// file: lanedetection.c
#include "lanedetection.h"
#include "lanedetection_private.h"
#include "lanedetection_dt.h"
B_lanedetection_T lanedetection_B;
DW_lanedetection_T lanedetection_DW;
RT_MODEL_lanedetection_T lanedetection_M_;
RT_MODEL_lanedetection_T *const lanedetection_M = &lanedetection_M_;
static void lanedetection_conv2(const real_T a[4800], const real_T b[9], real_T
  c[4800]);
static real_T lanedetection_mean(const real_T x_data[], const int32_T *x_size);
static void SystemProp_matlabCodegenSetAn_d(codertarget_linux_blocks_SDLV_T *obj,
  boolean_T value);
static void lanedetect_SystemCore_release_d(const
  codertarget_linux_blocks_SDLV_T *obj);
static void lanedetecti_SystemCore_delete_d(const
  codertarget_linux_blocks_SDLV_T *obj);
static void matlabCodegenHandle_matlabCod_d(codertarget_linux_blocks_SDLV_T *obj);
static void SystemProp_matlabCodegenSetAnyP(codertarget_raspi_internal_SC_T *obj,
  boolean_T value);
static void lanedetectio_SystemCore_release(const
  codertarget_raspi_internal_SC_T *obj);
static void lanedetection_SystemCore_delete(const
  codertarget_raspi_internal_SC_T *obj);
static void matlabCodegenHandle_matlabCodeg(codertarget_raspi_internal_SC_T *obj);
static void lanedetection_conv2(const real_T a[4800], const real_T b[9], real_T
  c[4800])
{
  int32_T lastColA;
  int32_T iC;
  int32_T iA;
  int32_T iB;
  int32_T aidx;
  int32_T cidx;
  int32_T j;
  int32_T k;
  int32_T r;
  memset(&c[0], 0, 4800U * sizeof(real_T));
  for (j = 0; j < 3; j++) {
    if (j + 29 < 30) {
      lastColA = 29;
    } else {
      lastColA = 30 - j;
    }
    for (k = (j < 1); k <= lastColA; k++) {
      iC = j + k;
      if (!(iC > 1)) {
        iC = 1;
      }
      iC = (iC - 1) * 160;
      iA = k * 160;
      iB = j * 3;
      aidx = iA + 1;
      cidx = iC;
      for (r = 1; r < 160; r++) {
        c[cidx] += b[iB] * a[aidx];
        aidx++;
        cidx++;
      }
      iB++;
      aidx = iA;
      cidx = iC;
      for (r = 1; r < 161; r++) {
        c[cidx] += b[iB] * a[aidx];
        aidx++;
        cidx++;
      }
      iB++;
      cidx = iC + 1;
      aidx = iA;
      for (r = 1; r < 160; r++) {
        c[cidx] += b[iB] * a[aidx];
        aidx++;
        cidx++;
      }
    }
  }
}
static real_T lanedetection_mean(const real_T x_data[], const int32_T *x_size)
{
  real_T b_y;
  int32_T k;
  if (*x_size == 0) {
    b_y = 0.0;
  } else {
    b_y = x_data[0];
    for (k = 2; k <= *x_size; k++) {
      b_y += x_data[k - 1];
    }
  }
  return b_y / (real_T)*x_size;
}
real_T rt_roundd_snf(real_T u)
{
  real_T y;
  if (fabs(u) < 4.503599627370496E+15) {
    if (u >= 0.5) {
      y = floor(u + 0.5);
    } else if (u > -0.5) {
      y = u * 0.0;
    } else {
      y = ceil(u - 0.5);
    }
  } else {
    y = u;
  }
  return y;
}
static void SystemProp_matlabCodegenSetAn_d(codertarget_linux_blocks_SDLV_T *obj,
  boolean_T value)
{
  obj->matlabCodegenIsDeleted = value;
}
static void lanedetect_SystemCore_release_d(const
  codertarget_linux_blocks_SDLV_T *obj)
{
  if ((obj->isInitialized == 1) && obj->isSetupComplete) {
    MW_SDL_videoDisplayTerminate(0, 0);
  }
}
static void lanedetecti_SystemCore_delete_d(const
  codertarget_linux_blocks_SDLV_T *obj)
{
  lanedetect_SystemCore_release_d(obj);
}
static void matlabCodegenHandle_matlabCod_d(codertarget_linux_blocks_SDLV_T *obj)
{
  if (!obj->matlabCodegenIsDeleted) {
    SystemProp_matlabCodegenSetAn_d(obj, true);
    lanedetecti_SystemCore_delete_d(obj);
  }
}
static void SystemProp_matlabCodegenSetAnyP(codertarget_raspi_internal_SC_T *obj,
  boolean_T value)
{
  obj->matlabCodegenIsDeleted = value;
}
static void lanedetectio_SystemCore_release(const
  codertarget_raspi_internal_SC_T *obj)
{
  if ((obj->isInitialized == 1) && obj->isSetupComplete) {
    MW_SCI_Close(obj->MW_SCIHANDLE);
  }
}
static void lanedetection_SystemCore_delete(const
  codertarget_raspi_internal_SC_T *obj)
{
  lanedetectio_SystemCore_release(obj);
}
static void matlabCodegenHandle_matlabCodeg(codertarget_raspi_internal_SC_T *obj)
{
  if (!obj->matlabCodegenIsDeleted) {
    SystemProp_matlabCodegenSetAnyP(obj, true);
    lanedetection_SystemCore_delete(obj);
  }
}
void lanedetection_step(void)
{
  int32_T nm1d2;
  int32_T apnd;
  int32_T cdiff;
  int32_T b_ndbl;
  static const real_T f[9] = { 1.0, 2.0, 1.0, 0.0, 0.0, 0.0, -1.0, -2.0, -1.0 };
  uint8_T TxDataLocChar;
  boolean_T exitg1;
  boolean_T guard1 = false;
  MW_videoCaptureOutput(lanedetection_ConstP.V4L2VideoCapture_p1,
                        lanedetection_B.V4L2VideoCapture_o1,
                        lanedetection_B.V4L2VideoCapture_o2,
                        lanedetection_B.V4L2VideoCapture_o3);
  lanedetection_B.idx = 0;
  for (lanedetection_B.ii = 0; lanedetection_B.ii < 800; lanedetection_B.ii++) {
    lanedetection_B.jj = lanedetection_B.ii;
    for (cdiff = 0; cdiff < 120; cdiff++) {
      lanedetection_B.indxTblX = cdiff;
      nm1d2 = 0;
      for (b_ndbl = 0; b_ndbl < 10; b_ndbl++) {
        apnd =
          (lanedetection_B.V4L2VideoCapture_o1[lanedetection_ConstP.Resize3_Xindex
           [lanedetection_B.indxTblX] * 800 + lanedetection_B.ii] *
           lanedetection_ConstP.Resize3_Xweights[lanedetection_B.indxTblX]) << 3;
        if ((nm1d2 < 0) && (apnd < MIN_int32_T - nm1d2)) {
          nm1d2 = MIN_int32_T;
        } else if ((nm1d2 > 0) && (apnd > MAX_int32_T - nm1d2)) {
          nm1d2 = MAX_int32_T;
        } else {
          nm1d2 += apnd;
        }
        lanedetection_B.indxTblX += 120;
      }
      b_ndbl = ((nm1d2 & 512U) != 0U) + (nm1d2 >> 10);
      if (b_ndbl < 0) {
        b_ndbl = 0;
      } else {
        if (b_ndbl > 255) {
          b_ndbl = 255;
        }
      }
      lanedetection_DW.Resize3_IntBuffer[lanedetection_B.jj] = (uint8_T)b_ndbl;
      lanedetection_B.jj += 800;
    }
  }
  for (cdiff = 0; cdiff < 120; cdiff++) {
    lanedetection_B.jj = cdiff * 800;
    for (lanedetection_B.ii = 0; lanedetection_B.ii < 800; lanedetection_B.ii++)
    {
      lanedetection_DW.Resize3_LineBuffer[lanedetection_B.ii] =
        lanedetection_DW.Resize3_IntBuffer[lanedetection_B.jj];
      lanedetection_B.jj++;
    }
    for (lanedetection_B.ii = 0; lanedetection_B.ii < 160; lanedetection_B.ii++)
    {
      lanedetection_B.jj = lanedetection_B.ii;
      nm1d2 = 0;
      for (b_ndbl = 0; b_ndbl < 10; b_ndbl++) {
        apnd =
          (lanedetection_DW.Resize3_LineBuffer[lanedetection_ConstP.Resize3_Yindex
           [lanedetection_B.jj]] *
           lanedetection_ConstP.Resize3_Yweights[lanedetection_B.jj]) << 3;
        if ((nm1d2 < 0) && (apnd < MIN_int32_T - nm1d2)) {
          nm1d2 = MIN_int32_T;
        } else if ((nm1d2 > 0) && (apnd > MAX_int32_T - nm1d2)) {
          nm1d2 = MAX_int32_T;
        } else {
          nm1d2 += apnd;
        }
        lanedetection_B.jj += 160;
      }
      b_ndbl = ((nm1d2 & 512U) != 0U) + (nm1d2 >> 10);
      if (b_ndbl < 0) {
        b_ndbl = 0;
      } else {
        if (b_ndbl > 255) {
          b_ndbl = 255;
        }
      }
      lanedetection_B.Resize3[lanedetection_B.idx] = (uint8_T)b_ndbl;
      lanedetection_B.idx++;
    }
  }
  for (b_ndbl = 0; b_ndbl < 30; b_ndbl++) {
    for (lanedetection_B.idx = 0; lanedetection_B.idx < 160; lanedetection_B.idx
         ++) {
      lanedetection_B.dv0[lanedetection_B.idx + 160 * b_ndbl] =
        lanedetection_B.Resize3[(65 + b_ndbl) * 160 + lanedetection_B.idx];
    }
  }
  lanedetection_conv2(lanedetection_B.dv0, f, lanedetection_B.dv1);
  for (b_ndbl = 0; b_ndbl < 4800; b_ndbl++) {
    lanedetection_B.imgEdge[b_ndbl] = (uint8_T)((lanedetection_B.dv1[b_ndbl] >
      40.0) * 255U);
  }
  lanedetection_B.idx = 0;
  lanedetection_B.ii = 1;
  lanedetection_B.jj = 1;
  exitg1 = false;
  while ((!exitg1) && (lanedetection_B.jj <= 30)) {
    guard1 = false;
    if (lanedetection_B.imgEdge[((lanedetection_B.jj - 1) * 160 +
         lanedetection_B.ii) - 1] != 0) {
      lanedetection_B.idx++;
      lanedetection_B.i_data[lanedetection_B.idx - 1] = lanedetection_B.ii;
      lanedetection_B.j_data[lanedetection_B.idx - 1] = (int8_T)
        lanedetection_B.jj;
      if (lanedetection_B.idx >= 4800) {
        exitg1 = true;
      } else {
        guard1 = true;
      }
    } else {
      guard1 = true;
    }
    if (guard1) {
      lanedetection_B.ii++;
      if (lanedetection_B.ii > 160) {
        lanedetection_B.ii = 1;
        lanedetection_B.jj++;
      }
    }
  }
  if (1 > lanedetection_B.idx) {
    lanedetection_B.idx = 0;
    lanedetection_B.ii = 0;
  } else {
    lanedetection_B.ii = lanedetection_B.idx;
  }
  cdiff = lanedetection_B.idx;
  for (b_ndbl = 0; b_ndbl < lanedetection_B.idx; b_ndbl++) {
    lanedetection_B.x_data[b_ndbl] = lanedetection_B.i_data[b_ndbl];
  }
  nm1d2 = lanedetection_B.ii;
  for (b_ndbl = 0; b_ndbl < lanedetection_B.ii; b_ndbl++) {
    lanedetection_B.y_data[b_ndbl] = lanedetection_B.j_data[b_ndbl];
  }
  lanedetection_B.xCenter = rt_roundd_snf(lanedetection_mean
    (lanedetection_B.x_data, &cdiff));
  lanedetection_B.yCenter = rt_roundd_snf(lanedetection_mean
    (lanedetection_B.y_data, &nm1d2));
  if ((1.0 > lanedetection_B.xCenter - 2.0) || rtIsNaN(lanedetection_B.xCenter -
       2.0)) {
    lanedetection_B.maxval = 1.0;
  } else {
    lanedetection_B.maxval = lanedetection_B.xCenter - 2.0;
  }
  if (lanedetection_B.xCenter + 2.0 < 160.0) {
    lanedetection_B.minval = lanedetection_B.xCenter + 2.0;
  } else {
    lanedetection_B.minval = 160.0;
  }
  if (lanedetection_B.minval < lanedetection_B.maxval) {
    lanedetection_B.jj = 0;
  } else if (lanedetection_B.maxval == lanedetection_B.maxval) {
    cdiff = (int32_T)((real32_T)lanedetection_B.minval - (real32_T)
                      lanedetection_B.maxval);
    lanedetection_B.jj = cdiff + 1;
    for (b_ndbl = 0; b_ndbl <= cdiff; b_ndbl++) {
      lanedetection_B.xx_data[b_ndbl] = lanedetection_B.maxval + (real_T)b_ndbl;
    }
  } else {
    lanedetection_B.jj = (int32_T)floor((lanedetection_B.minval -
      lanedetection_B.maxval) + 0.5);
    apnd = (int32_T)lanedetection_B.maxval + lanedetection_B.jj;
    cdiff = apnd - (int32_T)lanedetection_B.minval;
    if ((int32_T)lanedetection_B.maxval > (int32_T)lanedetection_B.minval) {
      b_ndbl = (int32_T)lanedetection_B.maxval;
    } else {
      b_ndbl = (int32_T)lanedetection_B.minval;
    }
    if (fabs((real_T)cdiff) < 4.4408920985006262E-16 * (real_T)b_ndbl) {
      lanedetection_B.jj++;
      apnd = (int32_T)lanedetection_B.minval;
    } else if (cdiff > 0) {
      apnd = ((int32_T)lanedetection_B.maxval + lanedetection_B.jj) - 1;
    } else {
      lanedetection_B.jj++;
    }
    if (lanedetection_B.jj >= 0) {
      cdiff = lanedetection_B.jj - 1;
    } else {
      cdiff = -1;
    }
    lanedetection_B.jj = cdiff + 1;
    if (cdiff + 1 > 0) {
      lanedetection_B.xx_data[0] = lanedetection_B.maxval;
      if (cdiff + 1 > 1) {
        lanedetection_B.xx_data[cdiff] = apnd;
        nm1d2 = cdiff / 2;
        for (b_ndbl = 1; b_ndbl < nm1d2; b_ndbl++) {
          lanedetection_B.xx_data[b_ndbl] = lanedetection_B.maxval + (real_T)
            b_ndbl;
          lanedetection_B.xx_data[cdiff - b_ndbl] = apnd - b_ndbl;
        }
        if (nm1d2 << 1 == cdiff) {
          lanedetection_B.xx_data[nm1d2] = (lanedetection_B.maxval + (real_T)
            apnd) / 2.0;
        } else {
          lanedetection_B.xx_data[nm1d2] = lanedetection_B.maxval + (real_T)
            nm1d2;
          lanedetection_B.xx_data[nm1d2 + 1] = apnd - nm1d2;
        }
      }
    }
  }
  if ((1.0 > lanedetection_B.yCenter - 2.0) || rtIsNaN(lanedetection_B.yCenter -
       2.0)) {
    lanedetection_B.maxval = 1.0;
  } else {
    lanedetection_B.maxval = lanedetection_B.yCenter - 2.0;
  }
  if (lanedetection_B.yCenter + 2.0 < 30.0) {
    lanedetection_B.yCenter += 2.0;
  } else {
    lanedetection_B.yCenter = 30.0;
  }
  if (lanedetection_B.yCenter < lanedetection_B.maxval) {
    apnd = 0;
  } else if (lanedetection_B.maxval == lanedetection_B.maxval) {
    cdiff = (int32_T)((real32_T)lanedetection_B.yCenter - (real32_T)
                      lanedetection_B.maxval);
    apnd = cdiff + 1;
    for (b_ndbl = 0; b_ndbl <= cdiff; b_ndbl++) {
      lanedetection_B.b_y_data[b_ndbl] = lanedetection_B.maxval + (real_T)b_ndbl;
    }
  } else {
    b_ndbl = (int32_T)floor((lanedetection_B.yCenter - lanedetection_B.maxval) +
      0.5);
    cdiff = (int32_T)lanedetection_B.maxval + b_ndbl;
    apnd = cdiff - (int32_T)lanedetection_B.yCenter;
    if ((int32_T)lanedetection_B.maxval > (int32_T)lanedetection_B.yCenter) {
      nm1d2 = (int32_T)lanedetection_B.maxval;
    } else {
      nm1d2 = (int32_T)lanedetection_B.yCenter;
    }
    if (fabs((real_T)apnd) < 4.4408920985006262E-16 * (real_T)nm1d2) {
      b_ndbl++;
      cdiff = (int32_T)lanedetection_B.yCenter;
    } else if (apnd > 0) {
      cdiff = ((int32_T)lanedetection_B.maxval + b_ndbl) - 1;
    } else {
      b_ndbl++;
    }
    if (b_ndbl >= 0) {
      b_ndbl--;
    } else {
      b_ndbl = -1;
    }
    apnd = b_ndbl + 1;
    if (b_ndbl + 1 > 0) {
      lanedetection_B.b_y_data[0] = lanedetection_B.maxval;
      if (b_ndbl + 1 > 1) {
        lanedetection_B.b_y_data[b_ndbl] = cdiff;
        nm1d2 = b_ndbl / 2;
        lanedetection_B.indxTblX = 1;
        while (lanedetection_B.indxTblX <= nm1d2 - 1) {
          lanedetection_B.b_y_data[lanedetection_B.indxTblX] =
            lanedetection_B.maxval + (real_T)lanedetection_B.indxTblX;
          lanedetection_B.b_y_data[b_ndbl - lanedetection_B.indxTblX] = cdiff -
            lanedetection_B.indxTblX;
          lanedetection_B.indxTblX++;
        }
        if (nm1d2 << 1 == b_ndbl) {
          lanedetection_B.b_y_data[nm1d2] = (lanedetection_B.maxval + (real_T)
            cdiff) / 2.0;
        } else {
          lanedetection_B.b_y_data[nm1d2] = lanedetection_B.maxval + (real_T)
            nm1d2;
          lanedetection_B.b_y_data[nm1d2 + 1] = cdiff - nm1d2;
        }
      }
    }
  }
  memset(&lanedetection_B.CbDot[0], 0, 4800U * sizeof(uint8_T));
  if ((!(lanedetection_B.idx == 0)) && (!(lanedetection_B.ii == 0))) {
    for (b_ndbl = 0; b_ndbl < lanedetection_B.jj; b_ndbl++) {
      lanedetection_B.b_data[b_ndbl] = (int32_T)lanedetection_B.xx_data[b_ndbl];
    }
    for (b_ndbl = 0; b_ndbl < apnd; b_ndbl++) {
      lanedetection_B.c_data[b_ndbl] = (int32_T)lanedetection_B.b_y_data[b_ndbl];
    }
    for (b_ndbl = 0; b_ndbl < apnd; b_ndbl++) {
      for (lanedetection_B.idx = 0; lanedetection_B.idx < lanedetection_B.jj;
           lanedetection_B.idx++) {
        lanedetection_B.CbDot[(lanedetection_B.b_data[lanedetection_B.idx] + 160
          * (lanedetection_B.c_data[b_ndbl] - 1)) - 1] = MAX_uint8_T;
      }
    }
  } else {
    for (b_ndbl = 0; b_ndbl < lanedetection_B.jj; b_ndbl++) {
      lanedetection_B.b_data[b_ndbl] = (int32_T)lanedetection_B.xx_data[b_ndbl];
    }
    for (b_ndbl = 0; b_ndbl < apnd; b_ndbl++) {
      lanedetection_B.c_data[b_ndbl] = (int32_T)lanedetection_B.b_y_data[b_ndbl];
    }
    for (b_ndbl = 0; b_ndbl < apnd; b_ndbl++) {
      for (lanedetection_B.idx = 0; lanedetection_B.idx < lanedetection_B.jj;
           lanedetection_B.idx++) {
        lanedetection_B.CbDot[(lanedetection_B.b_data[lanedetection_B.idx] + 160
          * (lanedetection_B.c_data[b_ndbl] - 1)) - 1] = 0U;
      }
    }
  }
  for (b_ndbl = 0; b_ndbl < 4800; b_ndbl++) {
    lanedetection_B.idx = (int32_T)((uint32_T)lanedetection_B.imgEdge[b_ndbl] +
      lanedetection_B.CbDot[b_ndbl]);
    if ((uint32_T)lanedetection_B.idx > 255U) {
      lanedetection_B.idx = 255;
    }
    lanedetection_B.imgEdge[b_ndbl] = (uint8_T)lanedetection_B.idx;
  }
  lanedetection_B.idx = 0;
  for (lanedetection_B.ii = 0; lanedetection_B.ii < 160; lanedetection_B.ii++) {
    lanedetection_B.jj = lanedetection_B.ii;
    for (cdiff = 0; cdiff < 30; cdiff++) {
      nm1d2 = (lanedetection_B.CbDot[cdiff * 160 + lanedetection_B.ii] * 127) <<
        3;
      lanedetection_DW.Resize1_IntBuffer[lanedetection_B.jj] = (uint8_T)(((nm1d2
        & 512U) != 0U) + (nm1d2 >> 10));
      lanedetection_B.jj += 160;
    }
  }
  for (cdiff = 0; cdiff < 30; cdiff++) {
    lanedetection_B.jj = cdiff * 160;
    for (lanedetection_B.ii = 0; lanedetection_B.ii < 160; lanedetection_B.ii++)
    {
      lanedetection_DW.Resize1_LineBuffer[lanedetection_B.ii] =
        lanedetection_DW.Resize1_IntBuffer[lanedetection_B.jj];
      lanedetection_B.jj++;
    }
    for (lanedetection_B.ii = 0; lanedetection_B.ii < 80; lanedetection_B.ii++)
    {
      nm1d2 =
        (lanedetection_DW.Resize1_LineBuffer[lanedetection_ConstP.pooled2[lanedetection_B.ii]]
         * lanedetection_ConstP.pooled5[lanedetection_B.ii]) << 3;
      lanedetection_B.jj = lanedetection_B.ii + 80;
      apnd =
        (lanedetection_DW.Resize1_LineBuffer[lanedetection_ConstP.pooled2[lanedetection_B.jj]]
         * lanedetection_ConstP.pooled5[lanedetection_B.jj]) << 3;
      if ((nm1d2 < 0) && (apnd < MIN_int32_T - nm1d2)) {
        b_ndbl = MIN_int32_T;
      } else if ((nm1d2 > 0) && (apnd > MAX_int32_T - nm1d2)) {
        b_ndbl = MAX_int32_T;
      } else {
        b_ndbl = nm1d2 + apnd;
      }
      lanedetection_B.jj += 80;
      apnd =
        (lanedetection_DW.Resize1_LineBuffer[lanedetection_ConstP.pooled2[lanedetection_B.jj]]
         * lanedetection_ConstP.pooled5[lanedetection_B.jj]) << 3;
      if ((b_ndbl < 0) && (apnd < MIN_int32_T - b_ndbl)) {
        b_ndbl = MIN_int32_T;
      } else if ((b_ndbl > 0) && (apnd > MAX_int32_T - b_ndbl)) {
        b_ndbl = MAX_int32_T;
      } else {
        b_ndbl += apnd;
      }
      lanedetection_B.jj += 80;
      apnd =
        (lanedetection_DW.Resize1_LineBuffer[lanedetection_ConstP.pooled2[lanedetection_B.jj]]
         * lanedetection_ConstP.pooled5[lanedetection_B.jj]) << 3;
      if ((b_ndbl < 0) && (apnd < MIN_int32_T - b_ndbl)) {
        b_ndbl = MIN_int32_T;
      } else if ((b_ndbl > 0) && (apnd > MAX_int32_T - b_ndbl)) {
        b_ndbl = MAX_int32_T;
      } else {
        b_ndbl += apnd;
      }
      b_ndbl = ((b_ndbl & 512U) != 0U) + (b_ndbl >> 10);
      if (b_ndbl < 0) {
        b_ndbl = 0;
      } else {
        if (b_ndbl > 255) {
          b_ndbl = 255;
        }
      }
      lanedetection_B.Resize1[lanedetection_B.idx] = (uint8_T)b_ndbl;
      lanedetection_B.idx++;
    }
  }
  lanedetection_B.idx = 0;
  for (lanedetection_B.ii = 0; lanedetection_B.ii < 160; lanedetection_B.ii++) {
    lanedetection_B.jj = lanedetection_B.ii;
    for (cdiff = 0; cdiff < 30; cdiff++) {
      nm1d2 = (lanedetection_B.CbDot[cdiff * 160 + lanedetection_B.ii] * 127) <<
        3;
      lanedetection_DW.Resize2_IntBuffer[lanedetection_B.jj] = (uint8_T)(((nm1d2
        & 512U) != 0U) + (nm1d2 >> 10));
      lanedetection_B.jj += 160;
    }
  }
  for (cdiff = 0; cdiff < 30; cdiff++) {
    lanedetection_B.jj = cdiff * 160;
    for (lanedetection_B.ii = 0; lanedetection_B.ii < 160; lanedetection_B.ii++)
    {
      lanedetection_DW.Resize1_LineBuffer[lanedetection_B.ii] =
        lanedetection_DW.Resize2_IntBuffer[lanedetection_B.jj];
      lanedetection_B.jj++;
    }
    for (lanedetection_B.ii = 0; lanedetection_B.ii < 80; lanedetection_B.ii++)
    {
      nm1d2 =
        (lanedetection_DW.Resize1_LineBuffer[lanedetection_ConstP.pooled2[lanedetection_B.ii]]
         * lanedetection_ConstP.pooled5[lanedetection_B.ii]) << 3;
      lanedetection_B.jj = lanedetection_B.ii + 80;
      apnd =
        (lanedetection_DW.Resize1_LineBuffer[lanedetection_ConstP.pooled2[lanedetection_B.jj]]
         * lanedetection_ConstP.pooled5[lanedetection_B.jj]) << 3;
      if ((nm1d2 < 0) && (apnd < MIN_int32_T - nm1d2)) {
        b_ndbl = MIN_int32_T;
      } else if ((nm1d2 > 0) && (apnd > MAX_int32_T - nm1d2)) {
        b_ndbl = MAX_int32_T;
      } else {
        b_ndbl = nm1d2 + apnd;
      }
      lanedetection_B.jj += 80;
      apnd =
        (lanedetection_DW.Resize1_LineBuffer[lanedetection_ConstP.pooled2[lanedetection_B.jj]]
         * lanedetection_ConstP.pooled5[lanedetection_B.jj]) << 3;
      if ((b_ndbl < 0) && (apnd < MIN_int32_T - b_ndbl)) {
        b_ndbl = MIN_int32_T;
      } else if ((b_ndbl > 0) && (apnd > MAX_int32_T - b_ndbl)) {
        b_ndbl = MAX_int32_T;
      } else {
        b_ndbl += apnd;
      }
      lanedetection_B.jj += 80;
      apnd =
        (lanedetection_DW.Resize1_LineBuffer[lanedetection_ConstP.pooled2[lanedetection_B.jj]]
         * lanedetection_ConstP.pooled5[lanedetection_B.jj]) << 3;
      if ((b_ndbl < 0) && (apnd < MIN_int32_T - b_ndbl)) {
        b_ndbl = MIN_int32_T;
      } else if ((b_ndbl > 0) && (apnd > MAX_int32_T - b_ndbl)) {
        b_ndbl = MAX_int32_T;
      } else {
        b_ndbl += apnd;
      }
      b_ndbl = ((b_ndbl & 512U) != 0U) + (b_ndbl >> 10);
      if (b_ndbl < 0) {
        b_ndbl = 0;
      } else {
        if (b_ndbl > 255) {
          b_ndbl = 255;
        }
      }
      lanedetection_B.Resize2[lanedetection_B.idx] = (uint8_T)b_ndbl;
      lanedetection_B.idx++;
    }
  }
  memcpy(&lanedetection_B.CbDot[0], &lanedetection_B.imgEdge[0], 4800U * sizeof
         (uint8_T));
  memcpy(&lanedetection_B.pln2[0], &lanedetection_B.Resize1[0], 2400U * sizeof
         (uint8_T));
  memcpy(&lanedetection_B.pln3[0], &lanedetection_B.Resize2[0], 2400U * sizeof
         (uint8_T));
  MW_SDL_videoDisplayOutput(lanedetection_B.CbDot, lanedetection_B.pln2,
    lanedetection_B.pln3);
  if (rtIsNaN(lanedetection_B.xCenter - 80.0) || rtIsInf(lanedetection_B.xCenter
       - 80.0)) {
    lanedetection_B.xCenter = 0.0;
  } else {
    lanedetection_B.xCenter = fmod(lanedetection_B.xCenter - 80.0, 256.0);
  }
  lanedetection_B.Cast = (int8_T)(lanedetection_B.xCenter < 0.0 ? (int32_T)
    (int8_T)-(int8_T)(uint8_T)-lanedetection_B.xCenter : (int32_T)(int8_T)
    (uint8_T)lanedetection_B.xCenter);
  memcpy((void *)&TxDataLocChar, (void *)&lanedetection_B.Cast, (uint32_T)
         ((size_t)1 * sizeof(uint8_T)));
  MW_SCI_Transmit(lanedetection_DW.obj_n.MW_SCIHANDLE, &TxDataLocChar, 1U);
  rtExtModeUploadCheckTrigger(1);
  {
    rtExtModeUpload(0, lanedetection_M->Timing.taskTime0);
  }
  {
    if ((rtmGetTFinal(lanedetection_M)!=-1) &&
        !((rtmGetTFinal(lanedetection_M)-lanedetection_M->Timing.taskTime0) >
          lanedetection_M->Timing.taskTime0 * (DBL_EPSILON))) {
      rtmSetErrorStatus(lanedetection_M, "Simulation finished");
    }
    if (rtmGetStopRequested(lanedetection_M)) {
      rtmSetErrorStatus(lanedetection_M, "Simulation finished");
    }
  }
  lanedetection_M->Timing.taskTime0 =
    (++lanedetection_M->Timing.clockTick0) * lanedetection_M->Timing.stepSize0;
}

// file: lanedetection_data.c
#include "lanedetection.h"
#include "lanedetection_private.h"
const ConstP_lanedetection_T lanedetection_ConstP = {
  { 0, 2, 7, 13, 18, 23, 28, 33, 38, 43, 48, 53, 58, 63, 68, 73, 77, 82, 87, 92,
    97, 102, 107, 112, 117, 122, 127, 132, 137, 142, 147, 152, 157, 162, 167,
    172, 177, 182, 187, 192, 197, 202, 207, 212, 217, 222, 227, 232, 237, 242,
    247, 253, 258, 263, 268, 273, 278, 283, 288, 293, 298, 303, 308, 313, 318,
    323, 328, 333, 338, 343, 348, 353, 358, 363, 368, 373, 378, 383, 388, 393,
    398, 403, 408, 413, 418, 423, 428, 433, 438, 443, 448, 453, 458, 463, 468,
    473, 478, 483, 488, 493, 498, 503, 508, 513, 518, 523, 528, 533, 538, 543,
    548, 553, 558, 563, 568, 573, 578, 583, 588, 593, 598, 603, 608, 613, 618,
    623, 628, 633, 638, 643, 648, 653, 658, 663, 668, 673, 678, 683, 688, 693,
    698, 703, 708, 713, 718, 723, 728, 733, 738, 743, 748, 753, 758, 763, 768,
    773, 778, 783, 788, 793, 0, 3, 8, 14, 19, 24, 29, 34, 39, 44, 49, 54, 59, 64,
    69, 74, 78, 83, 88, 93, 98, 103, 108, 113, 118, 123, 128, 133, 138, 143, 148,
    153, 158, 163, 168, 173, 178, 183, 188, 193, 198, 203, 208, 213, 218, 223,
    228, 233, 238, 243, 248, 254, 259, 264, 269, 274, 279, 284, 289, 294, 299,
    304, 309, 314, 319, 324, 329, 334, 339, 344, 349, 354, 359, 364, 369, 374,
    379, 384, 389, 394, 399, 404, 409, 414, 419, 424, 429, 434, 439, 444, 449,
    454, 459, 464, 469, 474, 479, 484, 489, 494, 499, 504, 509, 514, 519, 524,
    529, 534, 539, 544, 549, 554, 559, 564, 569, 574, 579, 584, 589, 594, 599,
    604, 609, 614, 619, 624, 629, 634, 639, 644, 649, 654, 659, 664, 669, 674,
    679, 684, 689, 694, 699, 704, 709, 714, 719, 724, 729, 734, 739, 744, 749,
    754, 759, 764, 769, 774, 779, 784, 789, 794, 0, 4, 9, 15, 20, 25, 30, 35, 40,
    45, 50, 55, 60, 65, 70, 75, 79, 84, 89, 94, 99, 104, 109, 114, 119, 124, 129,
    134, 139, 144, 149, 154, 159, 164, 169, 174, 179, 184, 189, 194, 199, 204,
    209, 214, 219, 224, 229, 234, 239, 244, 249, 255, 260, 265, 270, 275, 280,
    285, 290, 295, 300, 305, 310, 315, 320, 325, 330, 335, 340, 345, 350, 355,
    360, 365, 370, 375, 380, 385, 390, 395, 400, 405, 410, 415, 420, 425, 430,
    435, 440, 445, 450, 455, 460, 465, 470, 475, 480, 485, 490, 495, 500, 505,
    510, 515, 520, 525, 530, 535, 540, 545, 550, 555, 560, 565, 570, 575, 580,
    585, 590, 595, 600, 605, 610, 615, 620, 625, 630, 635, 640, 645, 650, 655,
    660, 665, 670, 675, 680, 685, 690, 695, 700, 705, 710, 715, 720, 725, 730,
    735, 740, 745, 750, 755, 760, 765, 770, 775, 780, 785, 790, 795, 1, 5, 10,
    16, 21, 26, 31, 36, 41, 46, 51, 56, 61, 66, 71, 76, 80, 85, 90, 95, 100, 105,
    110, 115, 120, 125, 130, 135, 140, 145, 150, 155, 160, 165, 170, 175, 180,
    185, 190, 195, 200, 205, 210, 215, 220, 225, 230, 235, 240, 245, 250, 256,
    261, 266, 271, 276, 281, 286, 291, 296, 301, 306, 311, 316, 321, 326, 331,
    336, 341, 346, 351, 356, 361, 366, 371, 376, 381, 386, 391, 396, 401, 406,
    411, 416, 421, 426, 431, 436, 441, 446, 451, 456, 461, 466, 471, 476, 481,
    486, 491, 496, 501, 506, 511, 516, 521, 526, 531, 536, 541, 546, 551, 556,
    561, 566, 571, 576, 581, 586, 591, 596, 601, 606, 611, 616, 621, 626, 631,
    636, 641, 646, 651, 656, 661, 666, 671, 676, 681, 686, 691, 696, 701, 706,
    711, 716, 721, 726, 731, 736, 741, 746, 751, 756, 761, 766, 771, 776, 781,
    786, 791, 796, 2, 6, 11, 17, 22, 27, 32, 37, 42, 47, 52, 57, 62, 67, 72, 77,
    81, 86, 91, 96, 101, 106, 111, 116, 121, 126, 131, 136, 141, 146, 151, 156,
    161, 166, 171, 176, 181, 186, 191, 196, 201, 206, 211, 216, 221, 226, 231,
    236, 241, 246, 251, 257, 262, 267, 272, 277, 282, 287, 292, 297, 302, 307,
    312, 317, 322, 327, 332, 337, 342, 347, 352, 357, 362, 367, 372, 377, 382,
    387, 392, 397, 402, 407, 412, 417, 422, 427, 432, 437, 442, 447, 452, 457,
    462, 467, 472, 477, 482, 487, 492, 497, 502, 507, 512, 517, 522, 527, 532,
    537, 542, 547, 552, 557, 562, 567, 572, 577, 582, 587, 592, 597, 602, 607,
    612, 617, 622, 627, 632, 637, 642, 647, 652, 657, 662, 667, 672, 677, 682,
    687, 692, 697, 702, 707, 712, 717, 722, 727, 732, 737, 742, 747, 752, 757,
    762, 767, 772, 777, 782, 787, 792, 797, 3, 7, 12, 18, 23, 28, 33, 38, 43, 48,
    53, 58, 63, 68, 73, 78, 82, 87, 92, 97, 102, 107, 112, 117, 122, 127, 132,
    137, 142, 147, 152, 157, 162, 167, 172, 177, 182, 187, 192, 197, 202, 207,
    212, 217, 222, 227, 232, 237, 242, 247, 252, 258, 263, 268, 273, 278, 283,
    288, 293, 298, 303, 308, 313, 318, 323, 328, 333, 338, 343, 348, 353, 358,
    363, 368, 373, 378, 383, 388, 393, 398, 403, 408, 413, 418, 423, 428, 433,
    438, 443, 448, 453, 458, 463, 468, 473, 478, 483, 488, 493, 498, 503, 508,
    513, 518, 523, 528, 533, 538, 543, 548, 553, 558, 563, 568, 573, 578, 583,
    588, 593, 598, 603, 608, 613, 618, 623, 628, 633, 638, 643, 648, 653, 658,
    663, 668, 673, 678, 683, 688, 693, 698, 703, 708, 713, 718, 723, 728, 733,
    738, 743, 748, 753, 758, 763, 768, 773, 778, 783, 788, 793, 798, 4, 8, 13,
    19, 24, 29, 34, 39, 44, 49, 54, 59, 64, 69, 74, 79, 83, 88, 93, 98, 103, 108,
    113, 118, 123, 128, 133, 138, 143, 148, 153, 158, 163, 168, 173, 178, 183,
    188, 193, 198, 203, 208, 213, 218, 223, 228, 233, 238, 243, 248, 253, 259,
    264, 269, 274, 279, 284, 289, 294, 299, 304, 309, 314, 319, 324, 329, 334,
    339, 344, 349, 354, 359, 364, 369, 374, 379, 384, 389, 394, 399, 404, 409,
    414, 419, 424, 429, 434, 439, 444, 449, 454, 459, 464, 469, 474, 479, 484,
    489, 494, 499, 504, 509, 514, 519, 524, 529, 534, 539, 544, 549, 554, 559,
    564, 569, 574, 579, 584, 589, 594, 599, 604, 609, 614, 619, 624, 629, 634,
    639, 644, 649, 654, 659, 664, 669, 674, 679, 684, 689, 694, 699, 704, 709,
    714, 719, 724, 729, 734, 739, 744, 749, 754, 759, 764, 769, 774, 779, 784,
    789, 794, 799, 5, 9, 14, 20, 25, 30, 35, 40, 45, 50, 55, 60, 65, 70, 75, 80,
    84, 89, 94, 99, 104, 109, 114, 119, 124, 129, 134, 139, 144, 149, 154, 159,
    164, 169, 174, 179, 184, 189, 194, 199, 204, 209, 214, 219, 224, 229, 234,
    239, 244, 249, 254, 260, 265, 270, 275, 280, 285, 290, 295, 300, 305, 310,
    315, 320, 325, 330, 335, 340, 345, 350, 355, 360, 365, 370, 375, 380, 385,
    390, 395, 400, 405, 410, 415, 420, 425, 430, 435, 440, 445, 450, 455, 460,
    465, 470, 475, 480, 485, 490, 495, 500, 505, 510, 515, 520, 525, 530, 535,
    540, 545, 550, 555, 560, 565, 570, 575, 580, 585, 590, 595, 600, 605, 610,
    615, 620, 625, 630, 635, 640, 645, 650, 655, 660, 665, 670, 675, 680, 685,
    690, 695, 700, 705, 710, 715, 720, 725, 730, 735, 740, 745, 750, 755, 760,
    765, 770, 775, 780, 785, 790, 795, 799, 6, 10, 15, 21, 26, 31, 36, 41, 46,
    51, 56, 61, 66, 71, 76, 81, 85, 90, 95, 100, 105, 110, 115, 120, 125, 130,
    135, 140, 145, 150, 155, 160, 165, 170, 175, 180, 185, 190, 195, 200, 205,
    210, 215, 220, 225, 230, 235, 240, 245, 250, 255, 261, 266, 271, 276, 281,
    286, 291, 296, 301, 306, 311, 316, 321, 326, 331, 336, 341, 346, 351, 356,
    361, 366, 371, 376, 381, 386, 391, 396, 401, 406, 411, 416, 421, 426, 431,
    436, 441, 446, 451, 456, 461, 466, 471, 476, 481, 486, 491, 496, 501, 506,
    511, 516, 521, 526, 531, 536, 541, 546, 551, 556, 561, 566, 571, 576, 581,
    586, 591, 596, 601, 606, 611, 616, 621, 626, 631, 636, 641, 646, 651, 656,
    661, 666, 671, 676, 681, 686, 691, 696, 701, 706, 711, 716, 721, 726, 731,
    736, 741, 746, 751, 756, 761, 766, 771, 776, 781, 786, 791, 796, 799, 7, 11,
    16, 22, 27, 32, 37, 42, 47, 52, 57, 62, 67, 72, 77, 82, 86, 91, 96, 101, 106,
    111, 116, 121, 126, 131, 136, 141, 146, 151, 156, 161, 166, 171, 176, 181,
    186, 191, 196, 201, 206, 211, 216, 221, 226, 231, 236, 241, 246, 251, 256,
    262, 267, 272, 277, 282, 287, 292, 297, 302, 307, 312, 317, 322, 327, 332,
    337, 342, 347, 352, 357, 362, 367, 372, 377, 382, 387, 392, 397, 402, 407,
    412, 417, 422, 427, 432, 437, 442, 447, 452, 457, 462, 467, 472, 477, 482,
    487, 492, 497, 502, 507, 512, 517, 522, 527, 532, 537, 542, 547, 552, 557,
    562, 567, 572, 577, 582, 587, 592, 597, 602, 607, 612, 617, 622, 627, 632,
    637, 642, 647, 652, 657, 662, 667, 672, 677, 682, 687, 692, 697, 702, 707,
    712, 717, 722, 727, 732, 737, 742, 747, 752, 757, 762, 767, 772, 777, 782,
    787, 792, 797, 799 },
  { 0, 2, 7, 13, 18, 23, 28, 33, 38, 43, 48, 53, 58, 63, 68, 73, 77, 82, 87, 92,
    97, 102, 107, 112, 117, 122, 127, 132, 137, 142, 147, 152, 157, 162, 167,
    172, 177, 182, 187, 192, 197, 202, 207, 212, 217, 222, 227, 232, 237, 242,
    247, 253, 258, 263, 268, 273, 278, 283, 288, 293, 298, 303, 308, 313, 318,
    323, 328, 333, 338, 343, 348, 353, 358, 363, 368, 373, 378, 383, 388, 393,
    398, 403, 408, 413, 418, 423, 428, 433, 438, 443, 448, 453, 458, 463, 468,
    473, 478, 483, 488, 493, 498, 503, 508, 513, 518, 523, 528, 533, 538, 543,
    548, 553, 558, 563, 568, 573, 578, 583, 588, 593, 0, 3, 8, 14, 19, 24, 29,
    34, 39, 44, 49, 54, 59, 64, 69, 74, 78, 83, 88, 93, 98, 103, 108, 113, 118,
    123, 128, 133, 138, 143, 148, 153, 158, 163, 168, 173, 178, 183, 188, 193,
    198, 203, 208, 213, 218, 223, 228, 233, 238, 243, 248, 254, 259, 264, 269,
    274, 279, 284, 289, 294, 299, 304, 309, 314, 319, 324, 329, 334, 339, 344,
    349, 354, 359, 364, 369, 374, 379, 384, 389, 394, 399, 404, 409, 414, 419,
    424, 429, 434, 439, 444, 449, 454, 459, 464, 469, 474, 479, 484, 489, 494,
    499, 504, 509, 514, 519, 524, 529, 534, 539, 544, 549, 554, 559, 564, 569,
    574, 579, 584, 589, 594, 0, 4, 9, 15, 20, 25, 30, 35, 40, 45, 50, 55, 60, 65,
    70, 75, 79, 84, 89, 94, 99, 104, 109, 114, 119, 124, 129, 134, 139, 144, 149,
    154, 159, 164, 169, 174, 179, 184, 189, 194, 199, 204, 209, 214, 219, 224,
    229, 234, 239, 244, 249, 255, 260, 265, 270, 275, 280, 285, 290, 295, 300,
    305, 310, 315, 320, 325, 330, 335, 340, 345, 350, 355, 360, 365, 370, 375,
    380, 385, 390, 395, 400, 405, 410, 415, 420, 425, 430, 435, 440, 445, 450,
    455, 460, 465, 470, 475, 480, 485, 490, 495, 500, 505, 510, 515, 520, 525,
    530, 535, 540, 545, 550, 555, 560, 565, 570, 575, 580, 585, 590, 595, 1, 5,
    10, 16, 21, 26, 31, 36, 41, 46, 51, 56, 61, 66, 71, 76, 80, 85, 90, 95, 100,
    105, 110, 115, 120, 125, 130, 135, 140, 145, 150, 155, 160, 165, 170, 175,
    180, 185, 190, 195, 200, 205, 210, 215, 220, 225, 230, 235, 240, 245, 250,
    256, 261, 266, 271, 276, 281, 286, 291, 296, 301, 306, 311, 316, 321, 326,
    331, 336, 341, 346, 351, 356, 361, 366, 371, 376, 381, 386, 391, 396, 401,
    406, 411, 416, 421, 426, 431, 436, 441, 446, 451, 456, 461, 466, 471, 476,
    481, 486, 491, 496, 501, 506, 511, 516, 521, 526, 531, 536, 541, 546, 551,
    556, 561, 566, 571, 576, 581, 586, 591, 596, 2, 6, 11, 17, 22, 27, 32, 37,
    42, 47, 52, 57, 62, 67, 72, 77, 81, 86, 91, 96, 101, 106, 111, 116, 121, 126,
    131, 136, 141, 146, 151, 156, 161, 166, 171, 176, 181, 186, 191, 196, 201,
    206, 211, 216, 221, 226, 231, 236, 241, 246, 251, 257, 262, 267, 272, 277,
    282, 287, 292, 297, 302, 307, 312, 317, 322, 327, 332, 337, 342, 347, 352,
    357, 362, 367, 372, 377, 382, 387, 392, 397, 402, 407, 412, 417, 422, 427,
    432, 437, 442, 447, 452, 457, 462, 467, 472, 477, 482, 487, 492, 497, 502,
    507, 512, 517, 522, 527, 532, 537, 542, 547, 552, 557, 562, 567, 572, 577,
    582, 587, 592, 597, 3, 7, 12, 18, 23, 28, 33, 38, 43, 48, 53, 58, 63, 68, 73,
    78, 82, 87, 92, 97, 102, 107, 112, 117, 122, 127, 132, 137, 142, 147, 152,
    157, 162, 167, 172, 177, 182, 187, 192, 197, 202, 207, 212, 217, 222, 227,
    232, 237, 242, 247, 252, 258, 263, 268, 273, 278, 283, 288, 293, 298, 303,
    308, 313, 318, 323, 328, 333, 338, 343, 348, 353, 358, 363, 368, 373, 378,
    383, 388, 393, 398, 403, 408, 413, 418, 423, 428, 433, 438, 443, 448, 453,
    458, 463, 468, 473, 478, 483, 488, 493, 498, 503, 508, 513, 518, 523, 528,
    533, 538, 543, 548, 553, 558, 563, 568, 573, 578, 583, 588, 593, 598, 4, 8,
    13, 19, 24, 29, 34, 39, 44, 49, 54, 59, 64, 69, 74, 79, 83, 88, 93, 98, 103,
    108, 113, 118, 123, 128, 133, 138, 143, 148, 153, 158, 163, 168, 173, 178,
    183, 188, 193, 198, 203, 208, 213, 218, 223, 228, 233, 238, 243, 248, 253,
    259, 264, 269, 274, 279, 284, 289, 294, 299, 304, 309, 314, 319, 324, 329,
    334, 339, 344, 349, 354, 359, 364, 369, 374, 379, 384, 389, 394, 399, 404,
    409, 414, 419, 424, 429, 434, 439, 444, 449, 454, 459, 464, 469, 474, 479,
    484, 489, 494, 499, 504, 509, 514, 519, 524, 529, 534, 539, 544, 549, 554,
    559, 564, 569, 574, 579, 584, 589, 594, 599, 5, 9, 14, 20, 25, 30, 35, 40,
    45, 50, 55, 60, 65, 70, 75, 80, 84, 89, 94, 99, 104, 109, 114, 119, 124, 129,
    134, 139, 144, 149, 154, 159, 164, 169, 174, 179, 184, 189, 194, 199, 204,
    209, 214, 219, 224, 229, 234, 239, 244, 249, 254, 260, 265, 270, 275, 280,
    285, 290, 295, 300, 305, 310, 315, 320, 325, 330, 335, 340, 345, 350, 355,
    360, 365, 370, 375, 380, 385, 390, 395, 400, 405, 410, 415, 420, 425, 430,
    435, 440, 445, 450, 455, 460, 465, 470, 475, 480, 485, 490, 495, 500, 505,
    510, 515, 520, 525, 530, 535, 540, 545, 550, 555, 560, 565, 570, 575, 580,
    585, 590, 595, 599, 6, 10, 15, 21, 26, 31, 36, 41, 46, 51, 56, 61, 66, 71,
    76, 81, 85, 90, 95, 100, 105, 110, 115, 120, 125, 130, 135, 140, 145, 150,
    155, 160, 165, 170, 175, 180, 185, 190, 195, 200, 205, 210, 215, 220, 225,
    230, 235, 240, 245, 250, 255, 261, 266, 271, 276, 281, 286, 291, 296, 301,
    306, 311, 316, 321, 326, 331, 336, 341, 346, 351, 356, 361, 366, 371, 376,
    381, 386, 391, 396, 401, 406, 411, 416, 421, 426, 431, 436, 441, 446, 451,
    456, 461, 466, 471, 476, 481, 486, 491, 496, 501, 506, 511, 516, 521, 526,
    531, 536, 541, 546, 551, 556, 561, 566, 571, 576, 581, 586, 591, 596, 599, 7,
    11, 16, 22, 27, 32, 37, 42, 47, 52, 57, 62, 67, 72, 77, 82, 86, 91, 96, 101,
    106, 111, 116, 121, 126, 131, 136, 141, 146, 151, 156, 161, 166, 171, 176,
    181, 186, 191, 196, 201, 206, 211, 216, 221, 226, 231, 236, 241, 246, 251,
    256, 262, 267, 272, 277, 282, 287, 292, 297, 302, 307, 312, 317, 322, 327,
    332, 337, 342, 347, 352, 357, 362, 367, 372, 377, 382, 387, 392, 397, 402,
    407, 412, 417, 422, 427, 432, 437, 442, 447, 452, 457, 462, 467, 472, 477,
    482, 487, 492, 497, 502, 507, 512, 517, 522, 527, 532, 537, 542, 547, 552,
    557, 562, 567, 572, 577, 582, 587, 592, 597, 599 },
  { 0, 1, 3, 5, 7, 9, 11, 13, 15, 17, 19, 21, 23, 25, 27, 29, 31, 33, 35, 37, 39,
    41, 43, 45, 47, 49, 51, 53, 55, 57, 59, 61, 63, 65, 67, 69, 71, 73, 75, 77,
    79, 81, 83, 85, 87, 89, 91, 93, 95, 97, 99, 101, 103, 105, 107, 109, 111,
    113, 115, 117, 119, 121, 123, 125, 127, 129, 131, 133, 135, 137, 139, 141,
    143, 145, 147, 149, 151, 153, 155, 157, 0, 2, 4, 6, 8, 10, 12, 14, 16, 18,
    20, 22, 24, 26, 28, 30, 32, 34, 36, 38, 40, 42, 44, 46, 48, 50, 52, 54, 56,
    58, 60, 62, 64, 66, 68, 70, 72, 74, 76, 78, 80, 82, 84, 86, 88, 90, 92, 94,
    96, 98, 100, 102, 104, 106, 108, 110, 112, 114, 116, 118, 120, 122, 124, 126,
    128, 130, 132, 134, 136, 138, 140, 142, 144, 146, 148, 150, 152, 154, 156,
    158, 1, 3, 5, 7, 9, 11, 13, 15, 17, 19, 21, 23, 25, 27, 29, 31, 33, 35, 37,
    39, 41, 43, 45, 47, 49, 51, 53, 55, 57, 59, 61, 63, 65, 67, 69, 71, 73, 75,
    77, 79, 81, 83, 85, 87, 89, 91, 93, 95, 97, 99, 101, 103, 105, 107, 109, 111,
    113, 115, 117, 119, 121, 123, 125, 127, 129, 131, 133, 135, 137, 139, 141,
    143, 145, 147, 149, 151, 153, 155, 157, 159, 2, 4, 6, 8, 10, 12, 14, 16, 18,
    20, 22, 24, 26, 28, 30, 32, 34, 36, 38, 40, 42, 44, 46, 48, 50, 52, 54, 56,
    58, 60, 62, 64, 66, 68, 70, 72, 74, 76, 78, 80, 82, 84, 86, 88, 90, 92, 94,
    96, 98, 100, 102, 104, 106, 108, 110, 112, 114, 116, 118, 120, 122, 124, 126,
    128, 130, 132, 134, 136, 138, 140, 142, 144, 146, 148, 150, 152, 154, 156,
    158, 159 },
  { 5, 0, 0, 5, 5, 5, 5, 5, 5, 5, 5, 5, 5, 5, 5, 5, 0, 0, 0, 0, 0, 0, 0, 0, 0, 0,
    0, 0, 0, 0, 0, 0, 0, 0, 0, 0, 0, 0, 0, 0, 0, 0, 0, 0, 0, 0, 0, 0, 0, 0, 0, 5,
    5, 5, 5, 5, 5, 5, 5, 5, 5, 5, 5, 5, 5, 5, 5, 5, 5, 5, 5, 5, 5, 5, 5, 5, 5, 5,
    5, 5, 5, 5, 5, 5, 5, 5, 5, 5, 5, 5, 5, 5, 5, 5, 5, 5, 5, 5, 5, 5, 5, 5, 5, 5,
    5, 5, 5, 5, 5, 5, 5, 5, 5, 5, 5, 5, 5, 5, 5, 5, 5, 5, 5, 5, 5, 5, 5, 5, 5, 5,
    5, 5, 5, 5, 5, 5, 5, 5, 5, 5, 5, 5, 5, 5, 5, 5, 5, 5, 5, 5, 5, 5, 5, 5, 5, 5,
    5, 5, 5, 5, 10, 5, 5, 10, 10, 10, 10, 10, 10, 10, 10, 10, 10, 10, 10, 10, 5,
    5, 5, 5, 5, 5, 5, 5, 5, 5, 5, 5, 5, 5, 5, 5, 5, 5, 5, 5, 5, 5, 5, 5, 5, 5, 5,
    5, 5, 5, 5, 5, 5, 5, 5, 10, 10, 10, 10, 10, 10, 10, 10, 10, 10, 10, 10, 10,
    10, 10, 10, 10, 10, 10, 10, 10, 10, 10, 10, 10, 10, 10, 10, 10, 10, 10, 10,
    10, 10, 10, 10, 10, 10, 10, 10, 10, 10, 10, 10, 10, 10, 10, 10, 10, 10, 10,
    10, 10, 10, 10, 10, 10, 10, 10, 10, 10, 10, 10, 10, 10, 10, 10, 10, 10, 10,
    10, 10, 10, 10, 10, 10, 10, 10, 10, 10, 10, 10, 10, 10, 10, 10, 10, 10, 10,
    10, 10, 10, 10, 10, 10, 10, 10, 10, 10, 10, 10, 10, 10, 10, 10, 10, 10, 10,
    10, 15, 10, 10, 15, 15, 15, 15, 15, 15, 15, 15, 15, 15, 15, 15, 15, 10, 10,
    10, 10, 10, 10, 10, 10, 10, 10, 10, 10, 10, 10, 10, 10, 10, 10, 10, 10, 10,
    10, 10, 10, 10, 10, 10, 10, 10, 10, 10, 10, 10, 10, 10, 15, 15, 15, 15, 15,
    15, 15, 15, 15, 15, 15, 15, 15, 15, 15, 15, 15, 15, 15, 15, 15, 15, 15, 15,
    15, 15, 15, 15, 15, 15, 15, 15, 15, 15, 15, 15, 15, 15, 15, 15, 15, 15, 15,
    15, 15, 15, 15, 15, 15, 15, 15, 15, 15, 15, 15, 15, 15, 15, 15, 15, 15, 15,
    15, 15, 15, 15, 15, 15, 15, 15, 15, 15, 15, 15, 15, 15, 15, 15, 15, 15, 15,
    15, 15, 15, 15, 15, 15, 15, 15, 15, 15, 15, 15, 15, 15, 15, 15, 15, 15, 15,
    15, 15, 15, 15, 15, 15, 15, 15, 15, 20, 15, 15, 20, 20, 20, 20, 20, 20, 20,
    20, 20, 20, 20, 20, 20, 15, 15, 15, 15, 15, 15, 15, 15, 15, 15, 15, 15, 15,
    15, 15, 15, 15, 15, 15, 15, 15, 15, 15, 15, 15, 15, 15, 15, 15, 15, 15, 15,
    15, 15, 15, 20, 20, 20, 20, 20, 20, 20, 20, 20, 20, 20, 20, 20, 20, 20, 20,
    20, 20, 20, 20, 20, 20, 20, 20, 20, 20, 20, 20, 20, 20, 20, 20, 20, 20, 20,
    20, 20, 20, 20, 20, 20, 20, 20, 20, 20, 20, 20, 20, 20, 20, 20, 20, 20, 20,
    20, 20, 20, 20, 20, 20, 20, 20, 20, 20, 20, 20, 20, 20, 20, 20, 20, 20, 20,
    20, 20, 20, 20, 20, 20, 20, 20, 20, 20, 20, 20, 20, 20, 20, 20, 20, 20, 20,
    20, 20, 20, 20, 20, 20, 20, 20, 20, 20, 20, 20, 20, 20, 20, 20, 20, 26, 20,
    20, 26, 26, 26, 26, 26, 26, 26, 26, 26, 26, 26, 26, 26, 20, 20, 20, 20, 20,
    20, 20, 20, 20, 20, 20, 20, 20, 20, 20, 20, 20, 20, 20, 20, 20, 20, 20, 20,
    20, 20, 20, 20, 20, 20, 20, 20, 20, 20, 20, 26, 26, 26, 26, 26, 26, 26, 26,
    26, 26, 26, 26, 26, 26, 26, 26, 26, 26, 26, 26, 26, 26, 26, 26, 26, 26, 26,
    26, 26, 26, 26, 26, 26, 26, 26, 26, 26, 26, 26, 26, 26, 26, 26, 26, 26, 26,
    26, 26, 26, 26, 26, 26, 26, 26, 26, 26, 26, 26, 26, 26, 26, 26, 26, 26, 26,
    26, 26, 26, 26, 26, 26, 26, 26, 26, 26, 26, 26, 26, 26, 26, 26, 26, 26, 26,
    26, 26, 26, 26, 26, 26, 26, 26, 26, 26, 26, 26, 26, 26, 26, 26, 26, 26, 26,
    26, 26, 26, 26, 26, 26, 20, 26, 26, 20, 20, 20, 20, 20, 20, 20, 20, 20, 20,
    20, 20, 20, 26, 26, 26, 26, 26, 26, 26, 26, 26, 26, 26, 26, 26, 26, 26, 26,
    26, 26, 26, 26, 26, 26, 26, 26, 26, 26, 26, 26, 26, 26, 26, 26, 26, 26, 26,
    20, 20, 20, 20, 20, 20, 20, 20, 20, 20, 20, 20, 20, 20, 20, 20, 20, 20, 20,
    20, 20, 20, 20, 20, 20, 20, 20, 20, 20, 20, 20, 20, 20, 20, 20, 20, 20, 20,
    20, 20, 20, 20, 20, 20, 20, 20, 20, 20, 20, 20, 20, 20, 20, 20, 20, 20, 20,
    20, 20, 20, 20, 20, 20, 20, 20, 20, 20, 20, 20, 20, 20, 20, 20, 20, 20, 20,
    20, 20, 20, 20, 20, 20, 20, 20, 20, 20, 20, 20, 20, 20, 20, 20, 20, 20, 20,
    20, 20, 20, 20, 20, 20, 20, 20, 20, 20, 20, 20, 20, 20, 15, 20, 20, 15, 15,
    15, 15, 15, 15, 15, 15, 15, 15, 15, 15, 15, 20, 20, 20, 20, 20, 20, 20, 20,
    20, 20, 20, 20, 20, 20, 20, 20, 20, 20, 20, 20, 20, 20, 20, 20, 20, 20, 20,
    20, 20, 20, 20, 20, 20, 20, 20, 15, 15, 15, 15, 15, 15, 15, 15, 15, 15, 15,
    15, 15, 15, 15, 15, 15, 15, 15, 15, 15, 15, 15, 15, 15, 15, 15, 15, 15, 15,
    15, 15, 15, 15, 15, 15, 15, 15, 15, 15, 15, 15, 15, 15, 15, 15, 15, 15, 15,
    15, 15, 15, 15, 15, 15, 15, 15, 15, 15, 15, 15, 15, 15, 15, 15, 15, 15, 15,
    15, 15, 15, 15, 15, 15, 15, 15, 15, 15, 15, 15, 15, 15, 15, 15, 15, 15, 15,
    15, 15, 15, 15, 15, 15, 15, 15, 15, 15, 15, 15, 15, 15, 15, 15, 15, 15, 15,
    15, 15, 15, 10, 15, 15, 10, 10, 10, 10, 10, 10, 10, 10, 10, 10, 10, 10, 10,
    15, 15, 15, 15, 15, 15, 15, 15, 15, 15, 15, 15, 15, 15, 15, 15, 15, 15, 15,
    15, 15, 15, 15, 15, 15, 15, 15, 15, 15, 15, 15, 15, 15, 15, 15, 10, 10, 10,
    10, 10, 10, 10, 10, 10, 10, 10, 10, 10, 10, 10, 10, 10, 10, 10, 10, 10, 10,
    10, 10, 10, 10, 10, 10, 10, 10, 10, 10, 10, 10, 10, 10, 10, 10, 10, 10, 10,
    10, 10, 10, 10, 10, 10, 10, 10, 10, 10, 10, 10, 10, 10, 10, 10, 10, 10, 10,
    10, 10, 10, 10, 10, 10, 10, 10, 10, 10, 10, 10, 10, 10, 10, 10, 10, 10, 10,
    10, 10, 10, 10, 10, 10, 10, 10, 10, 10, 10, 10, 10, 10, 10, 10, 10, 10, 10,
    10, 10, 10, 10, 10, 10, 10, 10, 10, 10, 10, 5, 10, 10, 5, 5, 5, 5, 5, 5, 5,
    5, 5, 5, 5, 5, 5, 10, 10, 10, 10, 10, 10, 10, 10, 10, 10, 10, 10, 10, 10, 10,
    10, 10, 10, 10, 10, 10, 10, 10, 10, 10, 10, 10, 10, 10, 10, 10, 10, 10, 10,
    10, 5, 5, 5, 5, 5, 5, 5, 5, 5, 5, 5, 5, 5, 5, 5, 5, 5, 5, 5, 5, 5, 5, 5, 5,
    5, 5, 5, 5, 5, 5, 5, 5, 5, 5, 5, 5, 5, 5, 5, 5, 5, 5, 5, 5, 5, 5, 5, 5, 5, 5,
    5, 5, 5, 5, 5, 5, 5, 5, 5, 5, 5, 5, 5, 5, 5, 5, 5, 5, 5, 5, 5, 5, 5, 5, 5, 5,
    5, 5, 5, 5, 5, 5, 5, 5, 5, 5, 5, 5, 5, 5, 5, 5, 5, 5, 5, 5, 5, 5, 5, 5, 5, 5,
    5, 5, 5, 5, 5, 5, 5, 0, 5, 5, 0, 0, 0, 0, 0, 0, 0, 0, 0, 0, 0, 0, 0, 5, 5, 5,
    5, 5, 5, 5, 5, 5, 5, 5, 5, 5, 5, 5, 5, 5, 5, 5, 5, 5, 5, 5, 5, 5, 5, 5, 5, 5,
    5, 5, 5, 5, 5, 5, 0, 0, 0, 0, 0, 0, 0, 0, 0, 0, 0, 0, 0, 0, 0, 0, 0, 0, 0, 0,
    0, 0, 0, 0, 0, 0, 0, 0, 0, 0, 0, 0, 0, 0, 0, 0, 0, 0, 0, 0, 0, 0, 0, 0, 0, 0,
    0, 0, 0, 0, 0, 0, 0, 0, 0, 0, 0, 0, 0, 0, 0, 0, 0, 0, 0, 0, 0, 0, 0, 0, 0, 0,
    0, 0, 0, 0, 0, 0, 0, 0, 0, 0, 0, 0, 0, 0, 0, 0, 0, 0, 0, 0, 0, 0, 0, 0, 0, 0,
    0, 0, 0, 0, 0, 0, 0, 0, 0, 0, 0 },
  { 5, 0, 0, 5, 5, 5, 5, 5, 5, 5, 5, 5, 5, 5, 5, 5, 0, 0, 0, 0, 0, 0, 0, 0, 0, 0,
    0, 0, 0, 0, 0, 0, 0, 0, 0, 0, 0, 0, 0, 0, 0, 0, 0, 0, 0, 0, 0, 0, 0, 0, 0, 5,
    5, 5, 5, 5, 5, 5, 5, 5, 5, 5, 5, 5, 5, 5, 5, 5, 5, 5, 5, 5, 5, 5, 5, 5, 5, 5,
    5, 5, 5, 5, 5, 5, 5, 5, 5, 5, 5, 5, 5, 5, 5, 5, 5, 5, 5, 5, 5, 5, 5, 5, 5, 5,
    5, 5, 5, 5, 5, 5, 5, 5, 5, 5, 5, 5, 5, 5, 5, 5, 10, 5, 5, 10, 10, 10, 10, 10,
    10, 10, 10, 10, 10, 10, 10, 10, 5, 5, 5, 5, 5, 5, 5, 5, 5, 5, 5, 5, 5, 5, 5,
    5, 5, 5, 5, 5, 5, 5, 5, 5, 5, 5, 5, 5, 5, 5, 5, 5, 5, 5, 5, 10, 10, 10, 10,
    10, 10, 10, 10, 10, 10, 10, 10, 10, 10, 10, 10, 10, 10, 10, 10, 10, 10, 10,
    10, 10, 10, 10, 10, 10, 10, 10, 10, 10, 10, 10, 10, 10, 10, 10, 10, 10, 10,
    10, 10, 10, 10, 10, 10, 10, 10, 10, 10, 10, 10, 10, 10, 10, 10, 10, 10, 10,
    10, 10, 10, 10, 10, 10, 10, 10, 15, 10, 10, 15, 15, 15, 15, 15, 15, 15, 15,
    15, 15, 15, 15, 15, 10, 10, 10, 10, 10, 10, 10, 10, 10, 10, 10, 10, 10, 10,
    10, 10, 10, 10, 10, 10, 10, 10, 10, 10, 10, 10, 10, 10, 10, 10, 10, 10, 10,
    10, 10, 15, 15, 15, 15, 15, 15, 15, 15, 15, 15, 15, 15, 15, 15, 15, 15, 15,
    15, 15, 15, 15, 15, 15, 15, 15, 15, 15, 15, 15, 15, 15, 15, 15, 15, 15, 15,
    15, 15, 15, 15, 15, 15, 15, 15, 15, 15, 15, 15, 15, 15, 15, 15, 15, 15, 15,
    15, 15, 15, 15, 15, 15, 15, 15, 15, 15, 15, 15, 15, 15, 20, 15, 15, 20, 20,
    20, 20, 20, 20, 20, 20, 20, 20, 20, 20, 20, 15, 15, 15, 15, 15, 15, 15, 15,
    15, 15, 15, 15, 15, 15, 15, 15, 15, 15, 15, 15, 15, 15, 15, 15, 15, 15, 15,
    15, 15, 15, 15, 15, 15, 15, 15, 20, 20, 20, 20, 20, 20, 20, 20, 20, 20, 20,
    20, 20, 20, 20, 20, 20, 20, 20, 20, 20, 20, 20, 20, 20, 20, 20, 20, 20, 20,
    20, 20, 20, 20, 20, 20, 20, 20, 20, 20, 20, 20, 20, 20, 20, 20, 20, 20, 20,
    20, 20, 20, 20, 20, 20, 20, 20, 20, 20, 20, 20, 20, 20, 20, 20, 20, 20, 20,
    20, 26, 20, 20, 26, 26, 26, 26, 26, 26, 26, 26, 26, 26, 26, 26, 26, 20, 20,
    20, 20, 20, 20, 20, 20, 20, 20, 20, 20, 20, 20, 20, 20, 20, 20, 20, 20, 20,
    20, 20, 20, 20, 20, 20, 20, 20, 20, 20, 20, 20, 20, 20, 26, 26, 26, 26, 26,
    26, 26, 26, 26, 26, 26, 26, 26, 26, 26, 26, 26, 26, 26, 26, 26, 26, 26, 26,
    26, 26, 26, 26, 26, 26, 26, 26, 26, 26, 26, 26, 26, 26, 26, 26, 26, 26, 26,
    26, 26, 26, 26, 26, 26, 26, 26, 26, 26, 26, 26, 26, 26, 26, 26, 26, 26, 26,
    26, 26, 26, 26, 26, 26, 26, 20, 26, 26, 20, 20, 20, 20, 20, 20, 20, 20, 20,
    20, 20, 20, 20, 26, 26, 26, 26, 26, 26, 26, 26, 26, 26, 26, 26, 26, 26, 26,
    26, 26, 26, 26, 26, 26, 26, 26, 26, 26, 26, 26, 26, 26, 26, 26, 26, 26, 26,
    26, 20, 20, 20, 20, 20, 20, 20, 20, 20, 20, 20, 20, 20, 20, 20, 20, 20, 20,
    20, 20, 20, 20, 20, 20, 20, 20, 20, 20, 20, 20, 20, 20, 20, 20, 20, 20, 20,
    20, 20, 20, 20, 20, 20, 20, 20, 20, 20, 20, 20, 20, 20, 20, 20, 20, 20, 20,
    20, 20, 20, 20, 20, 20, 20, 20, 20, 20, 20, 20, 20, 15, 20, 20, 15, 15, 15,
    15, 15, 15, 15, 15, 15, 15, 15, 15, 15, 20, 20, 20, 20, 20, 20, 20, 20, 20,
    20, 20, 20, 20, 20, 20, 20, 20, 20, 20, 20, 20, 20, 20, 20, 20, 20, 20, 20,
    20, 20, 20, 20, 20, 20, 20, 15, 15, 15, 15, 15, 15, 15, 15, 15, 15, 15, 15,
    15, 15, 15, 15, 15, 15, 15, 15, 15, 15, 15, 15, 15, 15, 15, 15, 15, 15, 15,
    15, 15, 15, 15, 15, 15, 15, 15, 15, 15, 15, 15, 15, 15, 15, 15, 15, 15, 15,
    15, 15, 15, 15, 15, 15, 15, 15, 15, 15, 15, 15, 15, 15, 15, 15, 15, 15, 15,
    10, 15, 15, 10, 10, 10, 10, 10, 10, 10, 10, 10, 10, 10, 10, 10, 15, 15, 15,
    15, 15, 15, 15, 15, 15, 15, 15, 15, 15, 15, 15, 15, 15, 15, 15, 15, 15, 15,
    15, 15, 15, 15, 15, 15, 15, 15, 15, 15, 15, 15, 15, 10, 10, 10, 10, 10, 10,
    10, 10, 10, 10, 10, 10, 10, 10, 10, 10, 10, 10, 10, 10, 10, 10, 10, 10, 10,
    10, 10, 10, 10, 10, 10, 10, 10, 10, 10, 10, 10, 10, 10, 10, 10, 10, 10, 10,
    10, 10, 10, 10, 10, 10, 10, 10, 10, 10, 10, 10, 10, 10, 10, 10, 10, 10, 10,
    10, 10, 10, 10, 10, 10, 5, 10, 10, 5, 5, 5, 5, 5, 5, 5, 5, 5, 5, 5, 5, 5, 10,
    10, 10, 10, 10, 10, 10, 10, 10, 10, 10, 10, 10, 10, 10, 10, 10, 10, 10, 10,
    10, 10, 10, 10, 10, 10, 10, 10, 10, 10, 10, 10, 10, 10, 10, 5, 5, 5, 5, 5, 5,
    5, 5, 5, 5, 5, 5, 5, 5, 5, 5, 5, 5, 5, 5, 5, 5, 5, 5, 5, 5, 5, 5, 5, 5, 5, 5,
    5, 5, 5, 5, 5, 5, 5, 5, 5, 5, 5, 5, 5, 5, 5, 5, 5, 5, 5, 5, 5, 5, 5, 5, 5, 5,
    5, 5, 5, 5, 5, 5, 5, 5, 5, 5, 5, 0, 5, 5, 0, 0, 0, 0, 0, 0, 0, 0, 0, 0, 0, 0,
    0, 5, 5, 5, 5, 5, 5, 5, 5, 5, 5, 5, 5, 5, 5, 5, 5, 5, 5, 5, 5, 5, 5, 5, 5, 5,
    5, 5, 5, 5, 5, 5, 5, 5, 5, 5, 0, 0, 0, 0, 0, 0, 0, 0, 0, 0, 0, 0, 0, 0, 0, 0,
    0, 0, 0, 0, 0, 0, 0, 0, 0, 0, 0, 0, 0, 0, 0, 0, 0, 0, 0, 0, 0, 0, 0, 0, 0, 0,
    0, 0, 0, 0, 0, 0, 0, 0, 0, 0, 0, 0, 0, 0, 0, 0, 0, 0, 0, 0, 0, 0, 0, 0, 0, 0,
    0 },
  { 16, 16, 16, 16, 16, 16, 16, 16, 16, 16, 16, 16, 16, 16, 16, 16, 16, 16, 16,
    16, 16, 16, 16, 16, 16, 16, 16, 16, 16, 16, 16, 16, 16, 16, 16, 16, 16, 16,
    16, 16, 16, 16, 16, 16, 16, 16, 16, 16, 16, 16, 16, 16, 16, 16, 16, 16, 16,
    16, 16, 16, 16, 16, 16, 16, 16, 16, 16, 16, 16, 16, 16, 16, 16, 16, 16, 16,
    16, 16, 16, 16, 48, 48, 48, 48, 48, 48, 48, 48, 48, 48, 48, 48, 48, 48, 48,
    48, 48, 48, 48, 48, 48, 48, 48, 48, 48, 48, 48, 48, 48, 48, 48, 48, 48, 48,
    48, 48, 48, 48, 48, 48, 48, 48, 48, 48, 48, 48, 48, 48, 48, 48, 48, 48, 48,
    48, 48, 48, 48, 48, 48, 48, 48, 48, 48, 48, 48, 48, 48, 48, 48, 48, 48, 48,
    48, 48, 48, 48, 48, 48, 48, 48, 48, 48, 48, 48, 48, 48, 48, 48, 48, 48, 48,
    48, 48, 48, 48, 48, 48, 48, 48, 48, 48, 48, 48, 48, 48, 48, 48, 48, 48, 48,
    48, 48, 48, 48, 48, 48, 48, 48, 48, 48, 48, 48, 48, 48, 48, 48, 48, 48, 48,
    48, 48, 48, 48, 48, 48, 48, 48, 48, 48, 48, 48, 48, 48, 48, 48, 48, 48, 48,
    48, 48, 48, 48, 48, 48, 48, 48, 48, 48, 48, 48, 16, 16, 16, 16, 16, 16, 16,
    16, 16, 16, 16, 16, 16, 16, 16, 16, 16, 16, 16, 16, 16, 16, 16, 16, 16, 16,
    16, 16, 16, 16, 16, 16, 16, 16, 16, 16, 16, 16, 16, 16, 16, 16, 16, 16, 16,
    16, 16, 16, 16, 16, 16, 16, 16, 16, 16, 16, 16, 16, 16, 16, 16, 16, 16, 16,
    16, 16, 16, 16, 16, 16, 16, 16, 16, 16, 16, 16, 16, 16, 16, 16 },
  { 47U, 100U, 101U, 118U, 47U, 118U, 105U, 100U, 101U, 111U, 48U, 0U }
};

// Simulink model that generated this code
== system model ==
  SerialWrite#1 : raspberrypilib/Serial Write  <- 1: Cast
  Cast : DataTypeConversion  <- 1: MATLABFunction#1/4
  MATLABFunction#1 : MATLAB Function  <- 1: MATLABFunction#2
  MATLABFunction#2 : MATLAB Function  <- 1: Resize3
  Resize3 : visiongeotforms/Resize  <- 1: V4L2VideoCapture
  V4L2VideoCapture : embdlinuxlib/V4L2 Video Capture
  SDLVideoDisplay#1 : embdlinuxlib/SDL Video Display  <- 1: MATLABFunction#1, 2: Resize1, 3: Resize2
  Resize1 : visiongeotforms/Resize  <- 1: MATLABFunction#1/2
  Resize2 : visiongeotforms/Resize  <- 1: MATLABFunction#1/3
== matlab function MATLABFunction#2 ==
function imgOUT   = imgROI(imgIN)

    % imgIN Array von 160x120
    % rectangle('Position',[x,y,w,h])
    
    imgOUT = imgIN(1:160,66:95);

end

== matlab function MATLABFunction#1 ==
function [imgEdge, CbDot, CrDot,  steeringAngle]  = lanedetection(imgCam)

    threshold = 40;
    
    % convert to grayscale
    % imgGray = rgb2gray(imgCam);

    % create laplacian filter
    k = [1 2 1; 0 0 0; -1 -2 -1];
    % run sobel
    V = conv2(double(imgCam),k','same');
    
    % filter edges
    imgEdges = uint8((V > threshold) * 255);
    
    % coordinates of all detected objects
    [x, y] = find(imgEdges);
    
    % detect the center of all objects
    xCenter = round(mean(x));
    yCenter = round(mean(y));
    
    % create vector xx and yy for an area around the center of all objects
    xx = max(1, xCenter-2):min(xCenter+2, size(imgEdges, 1));
    yy = max(1, yCenter-2):min(yCenter+2, size(imgEdges, 2));
    
    % create new array with the size of "bw" and fill it with "0"
    bwdot = zeros(size(imgEdges), 'uint8');
    
    % if there is something detected at x and y...
    if ~isempty(x) && ~isempty(y)
        % ...mark the area around the center
        bwdot(xx, yy) = 255;
    % if nothing gets detected...
    else
        bwdot(xx, yy) = 0;
    end
    
    % add the marked area around the center to the array justRed
    imgEdge = imgEdges + bwdot;
    CbDot = bwdot;
    CrDot = bwdot;
    steeringAngle = (xCenter - 80);
end
